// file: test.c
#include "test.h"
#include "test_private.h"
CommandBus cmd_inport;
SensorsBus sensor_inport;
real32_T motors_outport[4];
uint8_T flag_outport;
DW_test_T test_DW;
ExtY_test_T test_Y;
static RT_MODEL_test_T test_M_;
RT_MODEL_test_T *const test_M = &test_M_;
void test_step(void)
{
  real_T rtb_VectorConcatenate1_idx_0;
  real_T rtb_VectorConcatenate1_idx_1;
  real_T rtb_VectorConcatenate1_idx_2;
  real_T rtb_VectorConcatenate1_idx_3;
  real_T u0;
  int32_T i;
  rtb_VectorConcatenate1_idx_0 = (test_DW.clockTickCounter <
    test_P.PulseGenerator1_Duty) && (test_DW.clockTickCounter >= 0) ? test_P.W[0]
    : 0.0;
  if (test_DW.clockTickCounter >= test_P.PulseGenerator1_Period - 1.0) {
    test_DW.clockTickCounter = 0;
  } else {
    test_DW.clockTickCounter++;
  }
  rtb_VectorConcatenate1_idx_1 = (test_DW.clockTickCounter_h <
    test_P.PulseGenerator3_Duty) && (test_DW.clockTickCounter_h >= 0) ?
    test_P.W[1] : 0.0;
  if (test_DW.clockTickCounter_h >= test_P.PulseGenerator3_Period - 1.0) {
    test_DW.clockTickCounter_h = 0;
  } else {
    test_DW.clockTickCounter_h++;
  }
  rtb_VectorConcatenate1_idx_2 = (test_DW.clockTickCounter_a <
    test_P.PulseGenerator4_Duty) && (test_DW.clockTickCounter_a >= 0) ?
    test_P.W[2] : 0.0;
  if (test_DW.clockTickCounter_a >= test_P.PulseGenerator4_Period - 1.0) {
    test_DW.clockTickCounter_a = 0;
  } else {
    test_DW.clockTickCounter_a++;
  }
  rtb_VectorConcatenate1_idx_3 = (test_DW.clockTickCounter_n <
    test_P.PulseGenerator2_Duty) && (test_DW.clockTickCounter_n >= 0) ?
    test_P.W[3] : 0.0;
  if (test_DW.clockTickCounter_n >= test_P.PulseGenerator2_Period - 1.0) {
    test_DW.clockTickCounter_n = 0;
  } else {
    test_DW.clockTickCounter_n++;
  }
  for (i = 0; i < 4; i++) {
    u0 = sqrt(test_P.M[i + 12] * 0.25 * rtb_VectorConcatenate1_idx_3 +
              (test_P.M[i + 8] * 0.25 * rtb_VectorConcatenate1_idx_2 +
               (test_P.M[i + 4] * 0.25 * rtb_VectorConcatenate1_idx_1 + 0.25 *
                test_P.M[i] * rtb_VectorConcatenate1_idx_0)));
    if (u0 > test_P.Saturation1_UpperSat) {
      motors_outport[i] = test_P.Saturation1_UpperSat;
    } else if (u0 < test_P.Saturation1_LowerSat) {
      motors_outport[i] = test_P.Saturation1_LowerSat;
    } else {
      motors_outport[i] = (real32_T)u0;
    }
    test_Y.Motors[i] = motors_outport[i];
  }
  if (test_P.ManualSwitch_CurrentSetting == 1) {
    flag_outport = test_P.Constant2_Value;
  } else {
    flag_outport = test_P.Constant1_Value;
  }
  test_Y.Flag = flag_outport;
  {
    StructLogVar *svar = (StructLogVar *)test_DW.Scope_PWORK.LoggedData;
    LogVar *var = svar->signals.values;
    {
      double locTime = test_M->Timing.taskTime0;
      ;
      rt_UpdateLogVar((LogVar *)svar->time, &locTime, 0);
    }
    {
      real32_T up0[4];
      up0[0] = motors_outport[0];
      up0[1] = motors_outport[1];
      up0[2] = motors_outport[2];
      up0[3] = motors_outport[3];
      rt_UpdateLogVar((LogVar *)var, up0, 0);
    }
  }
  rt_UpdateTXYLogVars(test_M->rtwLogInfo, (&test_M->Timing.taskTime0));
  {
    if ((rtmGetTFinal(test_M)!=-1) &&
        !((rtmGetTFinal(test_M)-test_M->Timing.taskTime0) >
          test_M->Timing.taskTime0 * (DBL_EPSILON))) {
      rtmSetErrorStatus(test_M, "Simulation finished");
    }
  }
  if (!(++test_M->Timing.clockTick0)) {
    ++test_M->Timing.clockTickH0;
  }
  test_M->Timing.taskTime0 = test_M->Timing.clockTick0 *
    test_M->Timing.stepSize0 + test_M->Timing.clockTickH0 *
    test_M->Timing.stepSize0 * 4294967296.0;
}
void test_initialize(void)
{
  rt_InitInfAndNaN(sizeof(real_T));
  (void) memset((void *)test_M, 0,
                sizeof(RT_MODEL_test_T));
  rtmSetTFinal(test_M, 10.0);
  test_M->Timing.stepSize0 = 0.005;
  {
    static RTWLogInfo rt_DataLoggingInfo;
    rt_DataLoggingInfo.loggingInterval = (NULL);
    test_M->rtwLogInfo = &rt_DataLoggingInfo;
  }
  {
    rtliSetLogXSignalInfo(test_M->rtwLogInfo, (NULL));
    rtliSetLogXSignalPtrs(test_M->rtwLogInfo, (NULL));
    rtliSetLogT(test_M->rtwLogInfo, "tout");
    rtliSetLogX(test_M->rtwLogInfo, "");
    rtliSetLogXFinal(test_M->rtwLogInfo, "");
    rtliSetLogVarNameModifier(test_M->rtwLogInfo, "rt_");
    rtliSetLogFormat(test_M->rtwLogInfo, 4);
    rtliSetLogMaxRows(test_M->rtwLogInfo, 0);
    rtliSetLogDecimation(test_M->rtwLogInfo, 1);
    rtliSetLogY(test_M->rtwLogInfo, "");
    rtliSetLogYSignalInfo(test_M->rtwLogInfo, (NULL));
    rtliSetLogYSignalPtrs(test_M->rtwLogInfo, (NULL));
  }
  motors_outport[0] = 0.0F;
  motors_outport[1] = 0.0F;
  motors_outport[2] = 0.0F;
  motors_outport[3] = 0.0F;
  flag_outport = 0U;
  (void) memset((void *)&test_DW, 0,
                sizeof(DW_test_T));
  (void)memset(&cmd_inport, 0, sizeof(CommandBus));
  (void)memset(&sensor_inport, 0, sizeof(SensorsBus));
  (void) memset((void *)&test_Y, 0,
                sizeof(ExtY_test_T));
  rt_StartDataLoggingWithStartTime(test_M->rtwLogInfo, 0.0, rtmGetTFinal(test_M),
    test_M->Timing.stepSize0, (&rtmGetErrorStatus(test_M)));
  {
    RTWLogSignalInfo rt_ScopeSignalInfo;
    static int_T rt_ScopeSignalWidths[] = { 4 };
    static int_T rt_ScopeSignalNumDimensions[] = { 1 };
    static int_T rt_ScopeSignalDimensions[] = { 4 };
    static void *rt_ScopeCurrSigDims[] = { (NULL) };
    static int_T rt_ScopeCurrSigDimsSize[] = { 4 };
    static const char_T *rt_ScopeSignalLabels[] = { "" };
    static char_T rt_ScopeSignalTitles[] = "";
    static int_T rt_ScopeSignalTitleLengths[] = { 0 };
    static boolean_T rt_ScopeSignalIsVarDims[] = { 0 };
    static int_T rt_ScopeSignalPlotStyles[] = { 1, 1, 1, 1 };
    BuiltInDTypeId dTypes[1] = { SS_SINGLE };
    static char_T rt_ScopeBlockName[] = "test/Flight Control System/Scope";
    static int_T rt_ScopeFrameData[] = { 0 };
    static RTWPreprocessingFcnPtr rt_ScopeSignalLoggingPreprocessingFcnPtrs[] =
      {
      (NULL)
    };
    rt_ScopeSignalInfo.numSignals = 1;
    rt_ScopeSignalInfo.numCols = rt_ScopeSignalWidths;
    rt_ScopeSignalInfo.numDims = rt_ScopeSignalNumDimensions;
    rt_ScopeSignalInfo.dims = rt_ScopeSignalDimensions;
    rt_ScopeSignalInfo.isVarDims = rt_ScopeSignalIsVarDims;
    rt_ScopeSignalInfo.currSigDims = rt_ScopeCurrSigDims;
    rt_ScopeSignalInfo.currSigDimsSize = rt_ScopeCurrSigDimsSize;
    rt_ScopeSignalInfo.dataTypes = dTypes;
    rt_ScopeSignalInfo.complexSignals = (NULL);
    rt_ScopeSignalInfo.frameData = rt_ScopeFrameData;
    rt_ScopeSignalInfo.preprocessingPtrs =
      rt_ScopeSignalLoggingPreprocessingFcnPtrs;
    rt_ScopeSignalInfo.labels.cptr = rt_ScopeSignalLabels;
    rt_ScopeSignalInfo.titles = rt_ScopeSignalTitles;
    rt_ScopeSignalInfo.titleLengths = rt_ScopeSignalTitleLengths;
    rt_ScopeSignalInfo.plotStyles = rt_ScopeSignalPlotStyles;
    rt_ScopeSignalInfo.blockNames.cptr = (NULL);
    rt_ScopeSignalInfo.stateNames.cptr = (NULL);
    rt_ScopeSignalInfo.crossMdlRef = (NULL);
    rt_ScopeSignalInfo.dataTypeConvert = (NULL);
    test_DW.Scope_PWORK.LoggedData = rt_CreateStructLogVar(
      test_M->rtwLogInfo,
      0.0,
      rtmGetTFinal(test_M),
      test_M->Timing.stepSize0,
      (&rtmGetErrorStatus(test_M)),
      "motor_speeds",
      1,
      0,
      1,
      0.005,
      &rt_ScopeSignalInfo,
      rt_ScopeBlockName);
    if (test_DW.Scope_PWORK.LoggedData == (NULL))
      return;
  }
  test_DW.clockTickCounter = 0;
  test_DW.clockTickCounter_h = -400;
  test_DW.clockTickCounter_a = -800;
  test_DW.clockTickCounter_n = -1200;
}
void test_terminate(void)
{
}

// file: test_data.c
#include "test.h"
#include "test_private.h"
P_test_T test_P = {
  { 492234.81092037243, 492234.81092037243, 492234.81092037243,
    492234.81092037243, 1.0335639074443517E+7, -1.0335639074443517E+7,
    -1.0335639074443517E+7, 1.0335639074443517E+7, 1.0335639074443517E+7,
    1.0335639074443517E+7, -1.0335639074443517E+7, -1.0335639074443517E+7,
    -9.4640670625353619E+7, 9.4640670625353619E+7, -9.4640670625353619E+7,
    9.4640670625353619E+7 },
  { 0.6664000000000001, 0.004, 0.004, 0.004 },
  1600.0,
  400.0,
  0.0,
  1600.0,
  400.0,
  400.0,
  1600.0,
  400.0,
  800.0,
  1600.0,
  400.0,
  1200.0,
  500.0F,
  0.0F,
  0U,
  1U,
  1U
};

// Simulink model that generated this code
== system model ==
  Inport#1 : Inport
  Inport#2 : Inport
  Motors : Outport  <- 1: Saturation1
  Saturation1 : Saturate  UpperLimit=500  LowerLimit=0  <- 1: Sqrt#1
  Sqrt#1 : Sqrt  <- 1: Gain#1
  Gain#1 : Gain  Gain=1/4*M  Multiplication=Matrix(K*u)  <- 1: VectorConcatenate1
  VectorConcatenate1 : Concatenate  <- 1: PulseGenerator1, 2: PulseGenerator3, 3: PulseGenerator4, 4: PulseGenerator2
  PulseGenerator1 : DiscretePulseGenerator  Amplitude=W(1)  Period=1600  PulseWidth=400
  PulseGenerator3 : DiscretePulseGenerator  Amplitude=W(2)  Period=1600  PulseWidth=400  PhaseDelay=400
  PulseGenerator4 : DiscretePulseGenerator  Amplitude=W(3)  Period=1600  PulseWidth=400  PhaseDelay=800
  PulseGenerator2 : DiscretePulseGenerator  Amplitude=W(4)  Period=1600  PulseWidth=400  PhaseDelay=1200
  Flag : Outport  <- 1: ManualSwitch
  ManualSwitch : ManualSwitch  <- 1: Constant2, 2: Constant1
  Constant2 : Constant  Value=0
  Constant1 : Constant
